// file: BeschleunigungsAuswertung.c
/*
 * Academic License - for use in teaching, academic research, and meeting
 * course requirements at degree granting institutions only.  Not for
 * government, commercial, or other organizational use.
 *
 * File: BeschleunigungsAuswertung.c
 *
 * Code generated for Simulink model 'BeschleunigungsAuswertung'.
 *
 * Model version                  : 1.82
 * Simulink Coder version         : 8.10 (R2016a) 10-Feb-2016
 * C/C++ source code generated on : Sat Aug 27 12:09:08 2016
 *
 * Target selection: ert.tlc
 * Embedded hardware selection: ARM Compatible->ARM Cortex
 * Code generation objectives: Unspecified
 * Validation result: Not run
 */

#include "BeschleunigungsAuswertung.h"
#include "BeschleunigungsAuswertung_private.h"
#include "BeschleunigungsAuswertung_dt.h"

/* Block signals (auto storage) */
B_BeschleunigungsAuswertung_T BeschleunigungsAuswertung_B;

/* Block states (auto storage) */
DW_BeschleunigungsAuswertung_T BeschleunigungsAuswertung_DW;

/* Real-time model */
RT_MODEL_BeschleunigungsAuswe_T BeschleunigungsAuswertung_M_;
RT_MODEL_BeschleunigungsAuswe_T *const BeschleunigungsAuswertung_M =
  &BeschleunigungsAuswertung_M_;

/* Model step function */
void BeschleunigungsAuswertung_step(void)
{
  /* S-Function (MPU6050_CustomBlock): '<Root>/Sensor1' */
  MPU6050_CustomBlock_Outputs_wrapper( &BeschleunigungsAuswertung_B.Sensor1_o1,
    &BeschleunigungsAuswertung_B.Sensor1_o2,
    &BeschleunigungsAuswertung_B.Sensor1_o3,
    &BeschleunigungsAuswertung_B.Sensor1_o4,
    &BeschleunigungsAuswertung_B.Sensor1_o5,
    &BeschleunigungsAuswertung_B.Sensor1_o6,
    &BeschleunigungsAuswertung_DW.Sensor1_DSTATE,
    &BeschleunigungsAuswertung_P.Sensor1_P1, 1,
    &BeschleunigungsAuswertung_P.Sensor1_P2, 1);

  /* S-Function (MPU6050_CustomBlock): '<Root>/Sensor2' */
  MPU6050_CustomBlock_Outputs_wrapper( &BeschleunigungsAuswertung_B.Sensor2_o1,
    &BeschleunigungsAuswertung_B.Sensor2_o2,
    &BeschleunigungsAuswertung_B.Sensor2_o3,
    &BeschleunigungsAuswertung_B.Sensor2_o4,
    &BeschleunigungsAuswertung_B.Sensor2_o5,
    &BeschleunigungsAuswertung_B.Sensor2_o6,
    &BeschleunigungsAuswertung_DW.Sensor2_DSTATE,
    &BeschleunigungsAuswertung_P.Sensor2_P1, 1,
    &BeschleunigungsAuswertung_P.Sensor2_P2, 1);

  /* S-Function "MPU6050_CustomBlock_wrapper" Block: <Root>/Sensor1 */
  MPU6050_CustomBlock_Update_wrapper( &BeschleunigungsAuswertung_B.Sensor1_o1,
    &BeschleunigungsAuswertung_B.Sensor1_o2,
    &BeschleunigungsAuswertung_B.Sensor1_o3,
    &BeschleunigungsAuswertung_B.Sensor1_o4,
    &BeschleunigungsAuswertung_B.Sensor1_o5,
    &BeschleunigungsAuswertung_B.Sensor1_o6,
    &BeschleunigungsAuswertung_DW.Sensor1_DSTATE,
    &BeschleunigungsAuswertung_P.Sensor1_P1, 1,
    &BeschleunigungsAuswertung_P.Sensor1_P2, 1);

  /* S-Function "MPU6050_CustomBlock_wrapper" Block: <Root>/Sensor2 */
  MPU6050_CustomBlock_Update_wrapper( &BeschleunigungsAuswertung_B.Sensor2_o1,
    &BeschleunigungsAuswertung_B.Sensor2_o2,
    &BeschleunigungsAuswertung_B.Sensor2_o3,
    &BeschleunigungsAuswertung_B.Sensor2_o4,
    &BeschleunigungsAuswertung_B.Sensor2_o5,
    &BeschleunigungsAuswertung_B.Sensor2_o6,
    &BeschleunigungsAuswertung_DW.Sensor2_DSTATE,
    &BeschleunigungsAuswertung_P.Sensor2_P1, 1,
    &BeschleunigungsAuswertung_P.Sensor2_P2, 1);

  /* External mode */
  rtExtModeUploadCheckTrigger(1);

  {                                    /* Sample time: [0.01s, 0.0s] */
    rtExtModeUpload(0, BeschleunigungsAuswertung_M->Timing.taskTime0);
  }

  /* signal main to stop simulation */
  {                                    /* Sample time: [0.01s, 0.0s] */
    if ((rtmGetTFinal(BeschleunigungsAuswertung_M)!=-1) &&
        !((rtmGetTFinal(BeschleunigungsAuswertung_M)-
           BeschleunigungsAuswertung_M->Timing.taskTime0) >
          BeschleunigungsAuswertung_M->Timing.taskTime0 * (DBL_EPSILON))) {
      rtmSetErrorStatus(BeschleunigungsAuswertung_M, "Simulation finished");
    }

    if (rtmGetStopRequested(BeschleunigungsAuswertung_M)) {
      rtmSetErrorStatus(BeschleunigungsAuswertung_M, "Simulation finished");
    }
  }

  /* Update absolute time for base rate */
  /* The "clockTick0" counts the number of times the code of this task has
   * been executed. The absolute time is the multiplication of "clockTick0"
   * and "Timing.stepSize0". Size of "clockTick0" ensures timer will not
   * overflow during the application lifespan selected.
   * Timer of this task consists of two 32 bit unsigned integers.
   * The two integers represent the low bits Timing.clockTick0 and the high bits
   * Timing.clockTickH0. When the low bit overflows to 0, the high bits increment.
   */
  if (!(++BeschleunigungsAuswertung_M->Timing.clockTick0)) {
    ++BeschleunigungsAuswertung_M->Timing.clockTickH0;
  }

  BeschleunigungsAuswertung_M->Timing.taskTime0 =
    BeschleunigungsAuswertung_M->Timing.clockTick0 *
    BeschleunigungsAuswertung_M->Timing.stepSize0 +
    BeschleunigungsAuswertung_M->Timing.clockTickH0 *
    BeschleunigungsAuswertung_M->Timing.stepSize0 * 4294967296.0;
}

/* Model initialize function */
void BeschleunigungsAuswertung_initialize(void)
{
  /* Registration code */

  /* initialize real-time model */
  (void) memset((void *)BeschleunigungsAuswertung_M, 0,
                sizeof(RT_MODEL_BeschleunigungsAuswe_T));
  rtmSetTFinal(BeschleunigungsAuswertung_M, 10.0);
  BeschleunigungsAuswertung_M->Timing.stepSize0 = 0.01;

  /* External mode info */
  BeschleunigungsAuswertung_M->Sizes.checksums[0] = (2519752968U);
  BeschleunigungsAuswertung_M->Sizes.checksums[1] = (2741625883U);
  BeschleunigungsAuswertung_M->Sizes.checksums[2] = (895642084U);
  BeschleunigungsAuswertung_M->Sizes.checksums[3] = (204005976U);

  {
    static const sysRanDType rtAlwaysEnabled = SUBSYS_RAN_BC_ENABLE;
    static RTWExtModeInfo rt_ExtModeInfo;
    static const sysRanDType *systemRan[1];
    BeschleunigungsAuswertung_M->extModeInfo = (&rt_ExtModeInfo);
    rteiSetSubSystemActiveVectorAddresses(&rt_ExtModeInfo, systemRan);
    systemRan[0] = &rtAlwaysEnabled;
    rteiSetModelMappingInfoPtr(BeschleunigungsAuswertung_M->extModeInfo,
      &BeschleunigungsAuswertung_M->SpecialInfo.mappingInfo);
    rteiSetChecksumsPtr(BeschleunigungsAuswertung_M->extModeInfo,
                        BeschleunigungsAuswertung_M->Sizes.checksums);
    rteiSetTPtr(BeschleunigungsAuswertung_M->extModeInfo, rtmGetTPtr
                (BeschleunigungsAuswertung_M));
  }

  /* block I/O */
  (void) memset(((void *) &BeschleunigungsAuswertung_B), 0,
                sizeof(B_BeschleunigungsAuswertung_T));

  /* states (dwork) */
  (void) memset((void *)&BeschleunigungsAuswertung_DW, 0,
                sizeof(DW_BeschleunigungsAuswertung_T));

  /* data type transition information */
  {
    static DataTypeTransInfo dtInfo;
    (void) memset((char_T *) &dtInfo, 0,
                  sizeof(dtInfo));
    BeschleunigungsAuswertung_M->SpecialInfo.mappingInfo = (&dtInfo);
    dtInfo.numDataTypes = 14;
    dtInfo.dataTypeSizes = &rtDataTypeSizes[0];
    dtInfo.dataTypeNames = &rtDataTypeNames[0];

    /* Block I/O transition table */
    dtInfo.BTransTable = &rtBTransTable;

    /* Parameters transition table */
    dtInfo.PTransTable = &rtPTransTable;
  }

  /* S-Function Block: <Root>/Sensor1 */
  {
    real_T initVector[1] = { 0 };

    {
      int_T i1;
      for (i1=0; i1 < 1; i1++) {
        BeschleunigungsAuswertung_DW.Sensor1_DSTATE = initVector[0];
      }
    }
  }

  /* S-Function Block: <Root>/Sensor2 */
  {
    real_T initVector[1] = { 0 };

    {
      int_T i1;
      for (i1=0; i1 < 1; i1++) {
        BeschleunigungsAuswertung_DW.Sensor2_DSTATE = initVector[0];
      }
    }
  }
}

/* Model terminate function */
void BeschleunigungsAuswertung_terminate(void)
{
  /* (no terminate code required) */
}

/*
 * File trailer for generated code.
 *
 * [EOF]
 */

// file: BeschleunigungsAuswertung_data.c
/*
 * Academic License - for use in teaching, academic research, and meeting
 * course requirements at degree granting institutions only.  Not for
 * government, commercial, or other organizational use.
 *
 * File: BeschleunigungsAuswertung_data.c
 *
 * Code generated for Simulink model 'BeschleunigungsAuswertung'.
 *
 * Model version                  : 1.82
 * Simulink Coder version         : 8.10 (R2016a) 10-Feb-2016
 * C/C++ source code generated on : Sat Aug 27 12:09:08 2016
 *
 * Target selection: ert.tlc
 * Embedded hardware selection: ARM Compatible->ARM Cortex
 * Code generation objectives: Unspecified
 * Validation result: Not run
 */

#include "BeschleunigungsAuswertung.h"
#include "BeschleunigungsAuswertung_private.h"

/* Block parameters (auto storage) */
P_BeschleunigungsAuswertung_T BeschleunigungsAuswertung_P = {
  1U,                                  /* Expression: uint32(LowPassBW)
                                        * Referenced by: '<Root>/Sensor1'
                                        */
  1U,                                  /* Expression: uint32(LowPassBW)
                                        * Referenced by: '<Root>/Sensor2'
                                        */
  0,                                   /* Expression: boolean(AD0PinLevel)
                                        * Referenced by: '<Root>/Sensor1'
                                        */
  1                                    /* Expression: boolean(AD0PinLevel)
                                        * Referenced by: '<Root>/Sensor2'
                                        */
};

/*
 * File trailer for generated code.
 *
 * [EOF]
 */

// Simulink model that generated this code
simulink model "BeschleunigungsAuswertung"  (R2016a)
settings: Solver=FixedStepAuto  StartTime=0.0  StopTime=10  FixedStep=0.01  RelTol=1e-3
StopFcn:
  | AuswertungSensorenBeschleunigung

== system BeschleunigungsAuswertung ==
  Sensor1 : S-Function  InitFcn=try, set_param(gcb,'FunctionName','MPU6050_CustomBlock'), end  FunctionName=MPU6050_CustomBlock  Parameters=boolean(AD0PinLevel),uint32(LowPassBW)  SFunctionModules=MPU6050_CustomBlock_wrapper  SFunctionDeploymentMode=off  EnableBusSupport=off  mask(S-Function Builder){AD0PinLevel=0, LowPassBW=260}
      mask prompts: AD0PinLevel "Logic-Level of AD0 Pin"; LowPassBW "Low-Pass-Bandwidth [Hz]"
      mask help: Simulink:masks:SFunctionBuilder_MD
      mask init:
      | val = [[.9  0.75 0.75 1 1 .9 .9 1]',[1 1 0.75 0.75 .9 .9 1 .9]'];try , sys = get_param(gcb,'SfunBuilderFcnName');if isempty(sys), sys = get_param(gcb,'FunctionName'); end,catch, sys = get_param(gcb,'FunctionName'); end
  Sensor2 : S-Function  InitFcn=try, set_param(gcb,'FunctionName','MPU6050_CustomBlock'), end  FunctionName=MPU6050_CustomBlock  Parameters=boolean(AD0PinLevel),uint32(LowPassBW)  SFunctionModules=MPU6050_CustomBlock_wrapper  SFunctionDeploymentMode=off  EnableBusSupport=off  mask(S-Function Builder){AD0PinLevel=1, LowPassBW=260}
      mask prompts: AD0PinLevel "Logic-Level of AD0 Pin"; LowPassBW "Low-Pass-Bandwidth [Hz]"
      mask help: Simulink:masks:SFunctionBuilder_MD
      mask init: same as BeschleunigungsAuswertung/Sensor1
  Terminator{,1..7} (8 alike) : Terminator
  To Workspace : ToWorkspace  VariableName=x1__dd  SaveFormat=Structure With Time  SampleTime=-1
  To Workspace1 : ToWorkspace  VariableName=y1__dd  SaveFormat=Structure With Time  SampleTime=-1
  To Workspace2 : ToWorkspace  VariableName=y2__dd  SaveFormat=Structure With Time  SampleTime=-1
  To Workspace3 : ToWorkspace  VariableName=x2__dd  SaveFormat=Structure With Time  SampleTime=-1
  wires:
  Sensor2/1 -> To Workspace3/1
  Sensor2/2 -> To Workspace2/1
  Sensor2/4 -> Terminator5/1
  Sensor2/5 -> Terminator6/1
  Sensor2/6 -> Terminator7/1
  Sensor1/1 -> To Workspace/1
  Sensor1/2 -> To Workspace1/1
  Sensor1/3 -> Terminator/1
  Sensor1/4 -> Terminator1/1
  Sensor1/5 -> Terminator2/1
  Sensor1/6 -> Terminator3/1
  Sensor2/3 -> Terminator4/1
